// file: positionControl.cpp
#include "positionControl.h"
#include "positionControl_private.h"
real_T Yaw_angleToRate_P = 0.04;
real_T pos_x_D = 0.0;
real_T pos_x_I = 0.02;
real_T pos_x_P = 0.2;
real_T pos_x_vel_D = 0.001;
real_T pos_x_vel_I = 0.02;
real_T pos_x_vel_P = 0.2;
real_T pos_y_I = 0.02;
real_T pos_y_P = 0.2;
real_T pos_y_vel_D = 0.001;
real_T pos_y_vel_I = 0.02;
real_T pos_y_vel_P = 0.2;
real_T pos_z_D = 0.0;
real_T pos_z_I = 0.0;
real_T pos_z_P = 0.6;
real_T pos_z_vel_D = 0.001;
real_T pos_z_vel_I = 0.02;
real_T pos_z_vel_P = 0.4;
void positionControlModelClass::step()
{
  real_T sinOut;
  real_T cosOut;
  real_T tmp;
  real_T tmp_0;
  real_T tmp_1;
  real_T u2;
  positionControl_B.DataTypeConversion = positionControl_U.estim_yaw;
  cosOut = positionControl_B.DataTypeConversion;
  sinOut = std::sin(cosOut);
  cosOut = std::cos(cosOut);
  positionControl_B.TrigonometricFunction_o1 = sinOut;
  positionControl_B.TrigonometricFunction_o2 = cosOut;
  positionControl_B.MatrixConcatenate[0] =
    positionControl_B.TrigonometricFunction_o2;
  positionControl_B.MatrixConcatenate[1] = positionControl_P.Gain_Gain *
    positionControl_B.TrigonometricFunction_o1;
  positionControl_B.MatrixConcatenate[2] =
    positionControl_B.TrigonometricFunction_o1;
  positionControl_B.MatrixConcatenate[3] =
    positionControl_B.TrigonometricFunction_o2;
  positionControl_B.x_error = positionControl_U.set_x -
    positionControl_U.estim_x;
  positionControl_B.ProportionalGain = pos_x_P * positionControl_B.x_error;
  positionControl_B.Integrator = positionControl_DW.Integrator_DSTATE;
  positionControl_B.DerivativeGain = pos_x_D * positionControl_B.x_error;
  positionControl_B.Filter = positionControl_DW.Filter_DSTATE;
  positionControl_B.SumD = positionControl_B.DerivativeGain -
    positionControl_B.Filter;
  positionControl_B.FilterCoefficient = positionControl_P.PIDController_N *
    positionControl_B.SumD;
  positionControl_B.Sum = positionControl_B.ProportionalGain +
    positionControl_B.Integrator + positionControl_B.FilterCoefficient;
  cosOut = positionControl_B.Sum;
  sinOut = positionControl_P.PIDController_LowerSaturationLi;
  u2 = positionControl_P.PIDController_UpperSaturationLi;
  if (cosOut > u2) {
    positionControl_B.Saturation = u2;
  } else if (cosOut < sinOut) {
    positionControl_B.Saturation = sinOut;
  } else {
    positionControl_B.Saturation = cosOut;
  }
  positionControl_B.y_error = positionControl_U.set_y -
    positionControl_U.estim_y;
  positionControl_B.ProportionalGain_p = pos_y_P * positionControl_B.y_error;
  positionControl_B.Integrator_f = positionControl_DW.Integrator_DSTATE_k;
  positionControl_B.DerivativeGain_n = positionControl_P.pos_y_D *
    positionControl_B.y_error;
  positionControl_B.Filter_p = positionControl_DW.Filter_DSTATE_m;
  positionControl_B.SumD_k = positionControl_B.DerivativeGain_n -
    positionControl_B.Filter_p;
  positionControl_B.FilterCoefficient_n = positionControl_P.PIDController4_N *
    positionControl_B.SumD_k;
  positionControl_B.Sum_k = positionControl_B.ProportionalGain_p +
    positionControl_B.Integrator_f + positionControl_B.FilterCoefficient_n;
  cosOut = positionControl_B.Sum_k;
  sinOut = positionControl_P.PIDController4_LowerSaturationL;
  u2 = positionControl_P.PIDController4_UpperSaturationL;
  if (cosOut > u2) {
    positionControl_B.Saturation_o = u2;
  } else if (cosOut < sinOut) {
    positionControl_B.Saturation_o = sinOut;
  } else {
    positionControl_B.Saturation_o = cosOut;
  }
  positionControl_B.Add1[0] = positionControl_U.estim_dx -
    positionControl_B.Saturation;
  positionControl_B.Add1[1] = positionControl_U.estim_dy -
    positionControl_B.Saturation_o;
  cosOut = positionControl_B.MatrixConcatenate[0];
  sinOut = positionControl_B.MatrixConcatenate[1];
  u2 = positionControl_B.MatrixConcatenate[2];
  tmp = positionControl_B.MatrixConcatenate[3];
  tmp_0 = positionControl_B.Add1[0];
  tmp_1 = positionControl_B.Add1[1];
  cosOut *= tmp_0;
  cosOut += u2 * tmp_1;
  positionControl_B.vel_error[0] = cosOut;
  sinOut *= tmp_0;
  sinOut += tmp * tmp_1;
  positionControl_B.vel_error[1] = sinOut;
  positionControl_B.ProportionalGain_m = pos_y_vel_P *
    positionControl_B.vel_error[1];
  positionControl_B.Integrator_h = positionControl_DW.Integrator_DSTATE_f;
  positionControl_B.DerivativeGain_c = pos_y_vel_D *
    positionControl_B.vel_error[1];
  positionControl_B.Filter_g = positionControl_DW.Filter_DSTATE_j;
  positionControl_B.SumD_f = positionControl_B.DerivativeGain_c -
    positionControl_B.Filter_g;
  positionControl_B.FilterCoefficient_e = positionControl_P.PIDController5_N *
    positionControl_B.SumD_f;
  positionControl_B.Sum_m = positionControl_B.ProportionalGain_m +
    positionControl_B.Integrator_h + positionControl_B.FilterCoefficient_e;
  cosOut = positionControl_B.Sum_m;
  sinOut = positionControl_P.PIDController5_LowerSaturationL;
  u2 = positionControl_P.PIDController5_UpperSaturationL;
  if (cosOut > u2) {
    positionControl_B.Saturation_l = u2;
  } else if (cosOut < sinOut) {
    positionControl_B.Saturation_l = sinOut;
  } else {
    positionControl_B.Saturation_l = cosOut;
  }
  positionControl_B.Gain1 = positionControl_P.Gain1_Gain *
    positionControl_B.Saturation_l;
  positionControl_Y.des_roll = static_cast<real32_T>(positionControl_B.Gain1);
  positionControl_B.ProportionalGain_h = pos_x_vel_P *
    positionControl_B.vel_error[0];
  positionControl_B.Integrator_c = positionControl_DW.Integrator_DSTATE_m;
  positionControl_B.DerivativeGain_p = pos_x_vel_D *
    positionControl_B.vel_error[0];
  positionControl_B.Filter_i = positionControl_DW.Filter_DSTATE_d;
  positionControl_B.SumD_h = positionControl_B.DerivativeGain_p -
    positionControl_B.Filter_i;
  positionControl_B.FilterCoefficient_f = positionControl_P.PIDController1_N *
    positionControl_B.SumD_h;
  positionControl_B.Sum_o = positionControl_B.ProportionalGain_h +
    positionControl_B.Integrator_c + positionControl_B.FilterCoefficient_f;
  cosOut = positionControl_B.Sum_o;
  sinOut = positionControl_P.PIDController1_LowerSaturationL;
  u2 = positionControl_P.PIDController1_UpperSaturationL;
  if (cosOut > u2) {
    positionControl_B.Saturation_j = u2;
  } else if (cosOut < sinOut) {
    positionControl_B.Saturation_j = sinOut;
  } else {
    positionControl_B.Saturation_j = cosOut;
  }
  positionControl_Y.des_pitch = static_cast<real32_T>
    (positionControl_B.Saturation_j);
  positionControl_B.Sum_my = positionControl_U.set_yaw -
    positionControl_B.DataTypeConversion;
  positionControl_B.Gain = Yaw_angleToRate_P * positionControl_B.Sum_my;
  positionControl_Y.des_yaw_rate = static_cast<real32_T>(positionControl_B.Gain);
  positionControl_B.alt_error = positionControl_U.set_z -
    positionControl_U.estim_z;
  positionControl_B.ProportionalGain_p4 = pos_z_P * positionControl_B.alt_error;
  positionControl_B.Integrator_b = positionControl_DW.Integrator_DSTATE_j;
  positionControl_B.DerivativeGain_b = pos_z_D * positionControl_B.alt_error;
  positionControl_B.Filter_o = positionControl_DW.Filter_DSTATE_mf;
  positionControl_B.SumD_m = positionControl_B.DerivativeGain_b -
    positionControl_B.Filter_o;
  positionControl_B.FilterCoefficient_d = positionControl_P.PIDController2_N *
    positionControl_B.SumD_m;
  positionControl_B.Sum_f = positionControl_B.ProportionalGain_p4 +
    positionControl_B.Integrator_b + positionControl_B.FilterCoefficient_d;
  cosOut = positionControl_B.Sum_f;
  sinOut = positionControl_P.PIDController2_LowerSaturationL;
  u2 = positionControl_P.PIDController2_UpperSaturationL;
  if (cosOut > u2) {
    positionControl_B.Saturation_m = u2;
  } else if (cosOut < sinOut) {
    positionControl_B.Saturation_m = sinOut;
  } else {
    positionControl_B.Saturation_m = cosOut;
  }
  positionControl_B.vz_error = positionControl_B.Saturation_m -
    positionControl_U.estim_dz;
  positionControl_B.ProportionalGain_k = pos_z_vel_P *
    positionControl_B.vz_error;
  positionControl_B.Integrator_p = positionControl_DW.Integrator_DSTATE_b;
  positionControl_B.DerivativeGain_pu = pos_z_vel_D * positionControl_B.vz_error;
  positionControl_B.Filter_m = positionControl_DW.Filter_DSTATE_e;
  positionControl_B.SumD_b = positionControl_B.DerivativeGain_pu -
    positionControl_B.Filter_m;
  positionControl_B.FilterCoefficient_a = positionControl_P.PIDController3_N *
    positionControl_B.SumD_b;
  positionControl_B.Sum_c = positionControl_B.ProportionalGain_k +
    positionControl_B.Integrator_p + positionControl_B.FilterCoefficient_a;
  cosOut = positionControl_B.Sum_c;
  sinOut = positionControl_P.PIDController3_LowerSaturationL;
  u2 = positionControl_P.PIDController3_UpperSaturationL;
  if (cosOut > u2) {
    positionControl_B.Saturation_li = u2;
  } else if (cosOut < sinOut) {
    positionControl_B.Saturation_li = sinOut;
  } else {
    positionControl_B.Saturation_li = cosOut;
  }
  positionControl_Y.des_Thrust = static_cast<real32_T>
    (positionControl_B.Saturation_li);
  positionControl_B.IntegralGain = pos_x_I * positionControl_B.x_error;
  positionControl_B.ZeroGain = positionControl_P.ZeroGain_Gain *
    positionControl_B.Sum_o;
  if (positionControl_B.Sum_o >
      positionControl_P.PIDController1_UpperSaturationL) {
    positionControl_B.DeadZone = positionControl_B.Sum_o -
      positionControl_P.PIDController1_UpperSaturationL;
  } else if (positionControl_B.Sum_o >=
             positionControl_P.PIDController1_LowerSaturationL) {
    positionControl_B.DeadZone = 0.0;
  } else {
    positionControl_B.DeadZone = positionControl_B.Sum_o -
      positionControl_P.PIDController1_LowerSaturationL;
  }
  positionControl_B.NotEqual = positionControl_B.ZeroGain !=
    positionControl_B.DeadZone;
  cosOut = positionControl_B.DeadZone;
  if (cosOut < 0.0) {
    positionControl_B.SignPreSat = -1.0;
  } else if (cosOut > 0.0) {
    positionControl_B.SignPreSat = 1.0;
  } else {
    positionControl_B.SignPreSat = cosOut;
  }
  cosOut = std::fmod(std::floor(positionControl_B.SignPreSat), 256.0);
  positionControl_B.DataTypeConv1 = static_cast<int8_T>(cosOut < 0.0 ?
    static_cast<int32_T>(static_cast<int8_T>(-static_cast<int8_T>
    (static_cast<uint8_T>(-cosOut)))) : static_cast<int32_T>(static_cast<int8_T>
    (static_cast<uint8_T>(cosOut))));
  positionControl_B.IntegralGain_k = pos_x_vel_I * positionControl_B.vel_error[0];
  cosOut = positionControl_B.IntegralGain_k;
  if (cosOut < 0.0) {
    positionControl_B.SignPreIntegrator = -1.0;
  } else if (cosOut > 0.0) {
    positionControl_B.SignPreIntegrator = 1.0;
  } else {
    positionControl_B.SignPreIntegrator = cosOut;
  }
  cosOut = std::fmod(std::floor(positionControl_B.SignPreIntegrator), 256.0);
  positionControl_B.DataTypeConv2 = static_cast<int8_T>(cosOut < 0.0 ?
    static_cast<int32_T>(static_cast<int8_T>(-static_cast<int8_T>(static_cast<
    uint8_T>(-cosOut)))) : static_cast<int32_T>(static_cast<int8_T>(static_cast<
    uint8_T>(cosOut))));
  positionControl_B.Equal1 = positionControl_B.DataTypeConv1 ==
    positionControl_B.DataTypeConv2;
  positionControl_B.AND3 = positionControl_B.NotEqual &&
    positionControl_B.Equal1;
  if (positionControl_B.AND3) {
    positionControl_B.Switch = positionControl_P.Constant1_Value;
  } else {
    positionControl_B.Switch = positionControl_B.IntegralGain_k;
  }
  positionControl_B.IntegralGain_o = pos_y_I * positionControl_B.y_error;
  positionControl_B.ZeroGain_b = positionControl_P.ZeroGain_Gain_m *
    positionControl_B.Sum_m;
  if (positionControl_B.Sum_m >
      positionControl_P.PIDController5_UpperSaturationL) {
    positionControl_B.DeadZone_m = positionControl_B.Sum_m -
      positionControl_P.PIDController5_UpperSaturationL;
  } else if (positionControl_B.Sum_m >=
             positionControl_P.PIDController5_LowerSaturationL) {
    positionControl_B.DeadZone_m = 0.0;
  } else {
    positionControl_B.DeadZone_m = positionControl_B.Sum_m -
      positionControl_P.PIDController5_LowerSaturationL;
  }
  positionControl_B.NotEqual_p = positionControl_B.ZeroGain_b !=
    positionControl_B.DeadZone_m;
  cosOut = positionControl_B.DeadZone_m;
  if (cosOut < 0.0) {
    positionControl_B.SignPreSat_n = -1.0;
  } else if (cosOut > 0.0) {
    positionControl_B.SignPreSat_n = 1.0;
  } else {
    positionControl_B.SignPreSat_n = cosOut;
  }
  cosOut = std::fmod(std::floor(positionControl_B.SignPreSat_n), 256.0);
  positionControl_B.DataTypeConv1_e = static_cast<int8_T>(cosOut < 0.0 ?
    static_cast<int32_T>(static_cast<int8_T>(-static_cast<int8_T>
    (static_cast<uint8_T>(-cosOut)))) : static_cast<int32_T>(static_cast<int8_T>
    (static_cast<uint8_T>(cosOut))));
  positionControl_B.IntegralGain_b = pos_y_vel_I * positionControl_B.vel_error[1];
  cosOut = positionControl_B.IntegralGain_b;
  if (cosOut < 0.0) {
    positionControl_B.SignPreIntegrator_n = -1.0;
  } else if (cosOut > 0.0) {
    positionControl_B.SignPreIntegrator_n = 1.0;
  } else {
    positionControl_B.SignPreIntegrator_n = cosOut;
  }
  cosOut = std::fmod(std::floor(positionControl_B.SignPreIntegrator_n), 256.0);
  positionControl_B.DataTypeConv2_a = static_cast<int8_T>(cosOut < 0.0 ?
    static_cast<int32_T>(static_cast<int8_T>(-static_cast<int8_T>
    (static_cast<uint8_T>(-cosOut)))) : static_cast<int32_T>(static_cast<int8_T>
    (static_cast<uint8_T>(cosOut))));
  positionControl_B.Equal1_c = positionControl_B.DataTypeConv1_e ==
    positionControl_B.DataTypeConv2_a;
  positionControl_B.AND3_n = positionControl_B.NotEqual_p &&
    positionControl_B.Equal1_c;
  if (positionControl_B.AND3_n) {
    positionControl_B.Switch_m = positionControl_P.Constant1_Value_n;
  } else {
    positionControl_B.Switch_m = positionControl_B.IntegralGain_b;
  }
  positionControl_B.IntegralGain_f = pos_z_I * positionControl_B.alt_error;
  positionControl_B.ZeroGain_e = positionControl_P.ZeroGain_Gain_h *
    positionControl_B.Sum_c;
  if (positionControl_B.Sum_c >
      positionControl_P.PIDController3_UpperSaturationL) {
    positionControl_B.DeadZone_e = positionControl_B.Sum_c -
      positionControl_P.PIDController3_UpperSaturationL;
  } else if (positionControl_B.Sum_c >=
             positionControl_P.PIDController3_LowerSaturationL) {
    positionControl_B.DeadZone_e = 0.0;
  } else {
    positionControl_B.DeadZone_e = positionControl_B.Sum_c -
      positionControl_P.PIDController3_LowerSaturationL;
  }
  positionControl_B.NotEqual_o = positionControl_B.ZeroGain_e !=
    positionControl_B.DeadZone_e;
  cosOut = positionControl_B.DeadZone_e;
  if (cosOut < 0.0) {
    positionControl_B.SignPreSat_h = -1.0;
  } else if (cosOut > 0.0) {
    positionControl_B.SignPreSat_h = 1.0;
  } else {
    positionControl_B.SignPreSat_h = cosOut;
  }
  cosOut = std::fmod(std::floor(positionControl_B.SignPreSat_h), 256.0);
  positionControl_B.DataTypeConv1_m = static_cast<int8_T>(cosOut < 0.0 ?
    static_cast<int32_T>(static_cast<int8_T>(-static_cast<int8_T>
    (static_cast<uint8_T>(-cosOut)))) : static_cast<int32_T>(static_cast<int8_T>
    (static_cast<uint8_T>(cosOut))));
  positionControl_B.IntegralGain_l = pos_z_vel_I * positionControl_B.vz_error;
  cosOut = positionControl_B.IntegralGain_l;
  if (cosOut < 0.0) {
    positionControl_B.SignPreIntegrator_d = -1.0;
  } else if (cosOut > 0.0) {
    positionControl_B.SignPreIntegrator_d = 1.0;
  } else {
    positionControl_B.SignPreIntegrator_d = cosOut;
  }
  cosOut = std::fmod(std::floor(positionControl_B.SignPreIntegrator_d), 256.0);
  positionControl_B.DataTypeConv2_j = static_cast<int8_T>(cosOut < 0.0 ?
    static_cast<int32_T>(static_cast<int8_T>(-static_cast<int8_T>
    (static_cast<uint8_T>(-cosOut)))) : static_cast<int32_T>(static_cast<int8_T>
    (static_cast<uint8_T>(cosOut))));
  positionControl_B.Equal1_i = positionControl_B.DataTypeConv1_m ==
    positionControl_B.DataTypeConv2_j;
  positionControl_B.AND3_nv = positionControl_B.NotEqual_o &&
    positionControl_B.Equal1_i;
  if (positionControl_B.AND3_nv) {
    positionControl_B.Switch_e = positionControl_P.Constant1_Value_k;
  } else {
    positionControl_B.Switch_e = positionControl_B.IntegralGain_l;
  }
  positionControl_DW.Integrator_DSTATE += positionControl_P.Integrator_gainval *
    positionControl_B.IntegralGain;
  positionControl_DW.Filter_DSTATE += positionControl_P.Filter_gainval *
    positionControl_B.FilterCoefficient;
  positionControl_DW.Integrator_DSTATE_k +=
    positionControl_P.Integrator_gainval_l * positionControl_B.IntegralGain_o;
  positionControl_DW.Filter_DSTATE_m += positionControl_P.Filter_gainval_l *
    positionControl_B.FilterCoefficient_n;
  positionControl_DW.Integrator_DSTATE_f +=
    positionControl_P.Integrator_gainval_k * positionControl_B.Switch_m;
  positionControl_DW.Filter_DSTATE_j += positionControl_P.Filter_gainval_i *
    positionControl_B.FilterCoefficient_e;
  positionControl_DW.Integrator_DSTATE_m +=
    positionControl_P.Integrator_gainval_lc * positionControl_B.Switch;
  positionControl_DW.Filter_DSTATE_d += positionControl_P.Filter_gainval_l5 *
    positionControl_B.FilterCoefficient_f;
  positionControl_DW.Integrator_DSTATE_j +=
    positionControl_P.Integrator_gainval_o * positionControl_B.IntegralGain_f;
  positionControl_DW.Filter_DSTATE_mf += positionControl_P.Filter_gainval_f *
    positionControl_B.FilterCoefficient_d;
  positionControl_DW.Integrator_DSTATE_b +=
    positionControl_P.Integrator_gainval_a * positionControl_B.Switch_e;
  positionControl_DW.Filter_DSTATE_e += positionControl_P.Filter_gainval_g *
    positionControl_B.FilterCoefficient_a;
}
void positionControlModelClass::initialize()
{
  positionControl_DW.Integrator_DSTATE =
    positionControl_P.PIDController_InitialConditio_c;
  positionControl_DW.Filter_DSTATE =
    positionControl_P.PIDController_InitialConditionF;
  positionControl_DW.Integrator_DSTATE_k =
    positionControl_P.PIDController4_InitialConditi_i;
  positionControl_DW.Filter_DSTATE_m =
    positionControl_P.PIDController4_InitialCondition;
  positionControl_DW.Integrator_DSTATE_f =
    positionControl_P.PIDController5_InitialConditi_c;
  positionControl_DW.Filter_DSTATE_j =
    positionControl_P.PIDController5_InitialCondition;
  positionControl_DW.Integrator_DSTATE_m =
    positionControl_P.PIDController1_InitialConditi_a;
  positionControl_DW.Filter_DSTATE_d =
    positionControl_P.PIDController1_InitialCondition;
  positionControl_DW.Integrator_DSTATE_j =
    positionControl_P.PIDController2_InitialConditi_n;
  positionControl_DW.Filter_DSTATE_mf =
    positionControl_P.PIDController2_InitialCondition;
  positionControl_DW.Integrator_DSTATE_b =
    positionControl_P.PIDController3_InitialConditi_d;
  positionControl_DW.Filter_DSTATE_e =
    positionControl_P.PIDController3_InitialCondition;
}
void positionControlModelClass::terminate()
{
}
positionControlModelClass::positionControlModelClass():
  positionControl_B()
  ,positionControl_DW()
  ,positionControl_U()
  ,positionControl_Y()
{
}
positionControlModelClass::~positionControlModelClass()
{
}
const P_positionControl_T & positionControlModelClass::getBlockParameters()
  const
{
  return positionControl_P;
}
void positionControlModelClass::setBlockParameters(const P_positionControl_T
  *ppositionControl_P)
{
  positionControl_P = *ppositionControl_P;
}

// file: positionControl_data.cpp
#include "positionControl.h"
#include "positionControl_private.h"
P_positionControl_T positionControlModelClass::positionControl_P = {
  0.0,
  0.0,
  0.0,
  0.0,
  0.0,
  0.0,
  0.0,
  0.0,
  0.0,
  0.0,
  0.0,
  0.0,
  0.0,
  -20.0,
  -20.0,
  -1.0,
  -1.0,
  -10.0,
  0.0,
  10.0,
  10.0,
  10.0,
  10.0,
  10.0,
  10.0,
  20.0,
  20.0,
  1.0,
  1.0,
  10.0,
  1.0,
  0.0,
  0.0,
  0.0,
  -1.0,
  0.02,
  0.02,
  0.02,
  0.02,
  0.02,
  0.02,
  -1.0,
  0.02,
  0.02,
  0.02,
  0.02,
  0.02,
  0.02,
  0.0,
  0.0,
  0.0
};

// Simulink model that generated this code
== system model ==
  estim_yaw : Inport
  set_yaw : Inport
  set_x : Inport
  set_y : Inport
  set_z : Inport
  estim_x : Inport
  estim_y : Inport
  estim_z : Inport
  estim_dx : Inport
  estim_dy : Inport
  estim_dz : Inport
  des_roll : Outport  <- 1: DataTypeConversion#1
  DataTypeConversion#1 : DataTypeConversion  <- 1: Gain1
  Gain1 : Gain  Gain=-1  <- 1: PIDController5
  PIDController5 : simulink/Continuous/PID Controller  Controller=PID  Form=Parallel  TimeDomain=Discrete-time  IntegratorMethod=Forward Euler  P=pos_y_vel_P  I=pos_y_vel_I  D=pos_y_vel_D  N=10  InitialConditionForIntegrator=0  ExternalReset=none  LimitOutput=on  UpperSaturationLimit=1  LowerSaturationLimit=-1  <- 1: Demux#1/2
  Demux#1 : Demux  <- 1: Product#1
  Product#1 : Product  Multiplication=Matrix(*)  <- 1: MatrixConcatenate, 2: Add1
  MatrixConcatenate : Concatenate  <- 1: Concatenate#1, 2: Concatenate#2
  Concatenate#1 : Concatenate  <- 1: TrigonometricFunction/2, 2: Gain
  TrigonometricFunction : Trigonometry  Operator=sincos  <- 1: DataTypeConversion
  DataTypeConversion : DataTypeConversion  <- 1: estim_yaw
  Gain : Gain  Gain=-1  <- 1: TrigonometricFunction
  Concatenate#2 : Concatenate  <- 1: TrigonometricFunction, 2: TrigonometricFunction/2
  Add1 : Sum  Inputs=-+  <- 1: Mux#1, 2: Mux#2
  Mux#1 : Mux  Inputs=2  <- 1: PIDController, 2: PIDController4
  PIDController : simulink/Continuous/PID Controller  Controller=PID  Form=Parallel  TimeDomain=Discrete-time  IntegratorMethod=Forward Euler  P=pos_x_P  I=pos_x_I  D=pos_x_D  N=10  InitialConditionForIntegrator=0  ExternalReset=none  LimitOutput=on  UpperSaturationLimit=20  LowerSaturationLimit=-20  <- 1: Sum#1
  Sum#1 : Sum  Inputs=+-  <- 1: set_x, 2: estim_x
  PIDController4 : simulink/Continuous/PID Controller  Controller=PID  Form=Parallel  TimeDomain=Discrete-time  IntegratorMethod=Forward Euler  P=pos_y_P  I=pos_y_I  D=pos_y_D  N=10  InitialConditionForIntegrator=0  ExternalReset=none  LimitOutput=on  UpperSaturationLimit=20  LowerSaturationLimit=-20  <- 1: Sum#2
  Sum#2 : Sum  Inputs=+-  <- 1: set_y, 2: estim_y
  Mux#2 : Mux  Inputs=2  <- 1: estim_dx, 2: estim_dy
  des_pitch : Outport  <- 1: DataTypeConversion#2
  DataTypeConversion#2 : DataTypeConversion  <- 1: PIDController1
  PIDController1 : simulink/Continuous/PID Controller  Controller=PID  Form=Parallel  TimeDomain=Discrete-time  IntegratorMethod=Forward Euler  P=pos_x_vel_P  I=pos_x_vel_I  D=pos_x_vel_D  N=10  InitialConditionForIntegrator=0  ExternalReset=none  LimitOutput=on  UpperSaturationLimit=1  LowerSaturationLimit=-1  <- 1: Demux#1
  des_yaw_rate : Outport  <- 1: DataTypeConversion#3
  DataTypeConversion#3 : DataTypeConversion  <- 1: Gain#1
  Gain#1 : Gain  Gain=Yaw_angleToRate_P  <- 1: Sum
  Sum : Sum  Inputs=+-  <- 1: set_yaw, 2: DataTypeConversion
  des_Thrust : Outport  <- 1: DataTypeConversion#4
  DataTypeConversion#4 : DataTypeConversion  <- 1: PIDController3
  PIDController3 : simulink/Continuous/PID Controller  Controller=PID  Form=Parallel  TimeDomain=Discrete-time  IntegratorMethod=Forward Euler  P=pos_z_vel_P  I=pos_z_vel_I  D=pos_z_vel_D  N=10  InitialConditionForIntegrator=0  ExternalReset=none  LimitOutput=on  UpperSaturationLimit=1  LowerSaturationLimit=0  <- 1: Sum#3
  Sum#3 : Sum  Inputs=+-  <- 1: PIDController2, 2: estim_dz
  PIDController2 : simulink/Continuous/PID Controller  Controller=PID  Form=Parallel  TimeDomain=Discrete-time  IntegratorMethod=Forward Euler  P=pos_z_P  I=pos_z_I  D=pos_z_D  N=10  InitialConditionForIntegrator=0  ExternalReset=none  LimitOutput=on  UpperSaturationLimit=10  LowerSaturationLimit=-10  <- 1: Sum#4
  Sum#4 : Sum  Inputs=+-  <- 1: set_z, 2: estim_z
